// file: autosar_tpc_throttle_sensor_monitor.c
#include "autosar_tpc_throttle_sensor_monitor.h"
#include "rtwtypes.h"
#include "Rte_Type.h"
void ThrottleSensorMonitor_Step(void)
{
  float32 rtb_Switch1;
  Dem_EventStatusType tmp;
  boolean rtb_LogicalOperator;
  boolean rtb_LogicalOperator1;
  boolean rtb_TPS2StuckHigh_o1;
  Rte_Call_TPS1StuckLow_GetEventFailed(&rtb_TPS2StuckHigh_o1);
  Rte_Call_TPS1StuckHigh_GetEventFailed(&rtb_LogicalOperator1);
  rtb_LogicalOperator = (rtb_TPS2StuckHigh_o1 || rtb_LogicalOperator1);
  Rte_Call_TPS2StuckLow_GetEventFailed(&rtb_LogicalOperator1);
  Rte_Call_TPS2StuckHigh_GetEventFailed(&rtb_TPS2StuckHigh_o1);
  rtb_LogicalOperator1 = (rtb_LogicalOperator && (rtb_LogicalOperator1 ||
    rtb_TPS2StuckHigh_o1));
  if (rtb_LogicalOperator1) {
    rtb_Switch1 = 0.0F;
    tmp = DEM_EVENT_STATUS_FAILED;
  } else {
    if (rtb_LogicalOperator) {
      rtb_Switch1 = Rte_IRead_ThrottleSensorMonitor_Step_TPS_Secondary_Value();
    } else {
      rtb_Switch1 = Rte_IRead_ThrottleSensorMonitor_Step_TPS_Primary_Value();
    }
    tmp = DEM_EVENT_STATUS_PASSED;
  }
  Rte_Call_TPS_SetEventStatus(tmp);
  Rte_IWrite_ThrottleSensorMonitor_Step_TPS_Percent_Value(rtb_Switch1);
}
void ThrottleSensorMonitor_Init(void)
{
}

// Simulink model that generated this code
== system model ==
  Inport#1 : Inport
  Inport#2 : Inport
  Outport#1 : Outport  <- 1: Switch1
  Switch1 : Switch  Criteria=u2 ~= 0  <- 1: Constant#1, 2: LogicalOperator1, 3: Switch#1
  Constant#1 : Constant  Value=0
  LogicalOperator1 : Logic  <- 1: LogicalOperator, 2: Logic#1
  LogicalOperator : Logic  Operator=OR  <- 1: TPS1StuckLow, 2: TPS1StuckHigh
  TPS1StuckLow : autosarlibdem/DiagnosticInfoCaller
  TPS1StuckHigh : autosarlibdem/DiagnosticInfoCaller
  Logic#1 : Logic  Operator=OR  <- 1: TPS2StuckLow, 2: TPS2StuckHigh
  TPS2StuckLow : autosarlibdem/DiagnosticInfoCaller
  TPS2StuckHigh : autosarlibdem/DiagnosticInfoCaller
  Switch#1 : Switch  Criteria=u2 ~= 0  <- 1: Inport#2, 2: LogicalOperator, 3: Inport#1
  TPS : autosarlibdem/DiagnosticMonitorCaller  <- 1: Switch#2
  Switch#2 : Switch  Criteria=u2 ~= 0  <- 1: Constant#2, 2: LogicalOperator1, 3: Constant#3
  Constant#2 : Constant  Value=Dem_EventStatusType.DEM_EVENT_STATUS_FAILED
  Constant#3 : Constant  Value=Dem_EventStatusType.DEM_EVENT_STATUS_PASSED
